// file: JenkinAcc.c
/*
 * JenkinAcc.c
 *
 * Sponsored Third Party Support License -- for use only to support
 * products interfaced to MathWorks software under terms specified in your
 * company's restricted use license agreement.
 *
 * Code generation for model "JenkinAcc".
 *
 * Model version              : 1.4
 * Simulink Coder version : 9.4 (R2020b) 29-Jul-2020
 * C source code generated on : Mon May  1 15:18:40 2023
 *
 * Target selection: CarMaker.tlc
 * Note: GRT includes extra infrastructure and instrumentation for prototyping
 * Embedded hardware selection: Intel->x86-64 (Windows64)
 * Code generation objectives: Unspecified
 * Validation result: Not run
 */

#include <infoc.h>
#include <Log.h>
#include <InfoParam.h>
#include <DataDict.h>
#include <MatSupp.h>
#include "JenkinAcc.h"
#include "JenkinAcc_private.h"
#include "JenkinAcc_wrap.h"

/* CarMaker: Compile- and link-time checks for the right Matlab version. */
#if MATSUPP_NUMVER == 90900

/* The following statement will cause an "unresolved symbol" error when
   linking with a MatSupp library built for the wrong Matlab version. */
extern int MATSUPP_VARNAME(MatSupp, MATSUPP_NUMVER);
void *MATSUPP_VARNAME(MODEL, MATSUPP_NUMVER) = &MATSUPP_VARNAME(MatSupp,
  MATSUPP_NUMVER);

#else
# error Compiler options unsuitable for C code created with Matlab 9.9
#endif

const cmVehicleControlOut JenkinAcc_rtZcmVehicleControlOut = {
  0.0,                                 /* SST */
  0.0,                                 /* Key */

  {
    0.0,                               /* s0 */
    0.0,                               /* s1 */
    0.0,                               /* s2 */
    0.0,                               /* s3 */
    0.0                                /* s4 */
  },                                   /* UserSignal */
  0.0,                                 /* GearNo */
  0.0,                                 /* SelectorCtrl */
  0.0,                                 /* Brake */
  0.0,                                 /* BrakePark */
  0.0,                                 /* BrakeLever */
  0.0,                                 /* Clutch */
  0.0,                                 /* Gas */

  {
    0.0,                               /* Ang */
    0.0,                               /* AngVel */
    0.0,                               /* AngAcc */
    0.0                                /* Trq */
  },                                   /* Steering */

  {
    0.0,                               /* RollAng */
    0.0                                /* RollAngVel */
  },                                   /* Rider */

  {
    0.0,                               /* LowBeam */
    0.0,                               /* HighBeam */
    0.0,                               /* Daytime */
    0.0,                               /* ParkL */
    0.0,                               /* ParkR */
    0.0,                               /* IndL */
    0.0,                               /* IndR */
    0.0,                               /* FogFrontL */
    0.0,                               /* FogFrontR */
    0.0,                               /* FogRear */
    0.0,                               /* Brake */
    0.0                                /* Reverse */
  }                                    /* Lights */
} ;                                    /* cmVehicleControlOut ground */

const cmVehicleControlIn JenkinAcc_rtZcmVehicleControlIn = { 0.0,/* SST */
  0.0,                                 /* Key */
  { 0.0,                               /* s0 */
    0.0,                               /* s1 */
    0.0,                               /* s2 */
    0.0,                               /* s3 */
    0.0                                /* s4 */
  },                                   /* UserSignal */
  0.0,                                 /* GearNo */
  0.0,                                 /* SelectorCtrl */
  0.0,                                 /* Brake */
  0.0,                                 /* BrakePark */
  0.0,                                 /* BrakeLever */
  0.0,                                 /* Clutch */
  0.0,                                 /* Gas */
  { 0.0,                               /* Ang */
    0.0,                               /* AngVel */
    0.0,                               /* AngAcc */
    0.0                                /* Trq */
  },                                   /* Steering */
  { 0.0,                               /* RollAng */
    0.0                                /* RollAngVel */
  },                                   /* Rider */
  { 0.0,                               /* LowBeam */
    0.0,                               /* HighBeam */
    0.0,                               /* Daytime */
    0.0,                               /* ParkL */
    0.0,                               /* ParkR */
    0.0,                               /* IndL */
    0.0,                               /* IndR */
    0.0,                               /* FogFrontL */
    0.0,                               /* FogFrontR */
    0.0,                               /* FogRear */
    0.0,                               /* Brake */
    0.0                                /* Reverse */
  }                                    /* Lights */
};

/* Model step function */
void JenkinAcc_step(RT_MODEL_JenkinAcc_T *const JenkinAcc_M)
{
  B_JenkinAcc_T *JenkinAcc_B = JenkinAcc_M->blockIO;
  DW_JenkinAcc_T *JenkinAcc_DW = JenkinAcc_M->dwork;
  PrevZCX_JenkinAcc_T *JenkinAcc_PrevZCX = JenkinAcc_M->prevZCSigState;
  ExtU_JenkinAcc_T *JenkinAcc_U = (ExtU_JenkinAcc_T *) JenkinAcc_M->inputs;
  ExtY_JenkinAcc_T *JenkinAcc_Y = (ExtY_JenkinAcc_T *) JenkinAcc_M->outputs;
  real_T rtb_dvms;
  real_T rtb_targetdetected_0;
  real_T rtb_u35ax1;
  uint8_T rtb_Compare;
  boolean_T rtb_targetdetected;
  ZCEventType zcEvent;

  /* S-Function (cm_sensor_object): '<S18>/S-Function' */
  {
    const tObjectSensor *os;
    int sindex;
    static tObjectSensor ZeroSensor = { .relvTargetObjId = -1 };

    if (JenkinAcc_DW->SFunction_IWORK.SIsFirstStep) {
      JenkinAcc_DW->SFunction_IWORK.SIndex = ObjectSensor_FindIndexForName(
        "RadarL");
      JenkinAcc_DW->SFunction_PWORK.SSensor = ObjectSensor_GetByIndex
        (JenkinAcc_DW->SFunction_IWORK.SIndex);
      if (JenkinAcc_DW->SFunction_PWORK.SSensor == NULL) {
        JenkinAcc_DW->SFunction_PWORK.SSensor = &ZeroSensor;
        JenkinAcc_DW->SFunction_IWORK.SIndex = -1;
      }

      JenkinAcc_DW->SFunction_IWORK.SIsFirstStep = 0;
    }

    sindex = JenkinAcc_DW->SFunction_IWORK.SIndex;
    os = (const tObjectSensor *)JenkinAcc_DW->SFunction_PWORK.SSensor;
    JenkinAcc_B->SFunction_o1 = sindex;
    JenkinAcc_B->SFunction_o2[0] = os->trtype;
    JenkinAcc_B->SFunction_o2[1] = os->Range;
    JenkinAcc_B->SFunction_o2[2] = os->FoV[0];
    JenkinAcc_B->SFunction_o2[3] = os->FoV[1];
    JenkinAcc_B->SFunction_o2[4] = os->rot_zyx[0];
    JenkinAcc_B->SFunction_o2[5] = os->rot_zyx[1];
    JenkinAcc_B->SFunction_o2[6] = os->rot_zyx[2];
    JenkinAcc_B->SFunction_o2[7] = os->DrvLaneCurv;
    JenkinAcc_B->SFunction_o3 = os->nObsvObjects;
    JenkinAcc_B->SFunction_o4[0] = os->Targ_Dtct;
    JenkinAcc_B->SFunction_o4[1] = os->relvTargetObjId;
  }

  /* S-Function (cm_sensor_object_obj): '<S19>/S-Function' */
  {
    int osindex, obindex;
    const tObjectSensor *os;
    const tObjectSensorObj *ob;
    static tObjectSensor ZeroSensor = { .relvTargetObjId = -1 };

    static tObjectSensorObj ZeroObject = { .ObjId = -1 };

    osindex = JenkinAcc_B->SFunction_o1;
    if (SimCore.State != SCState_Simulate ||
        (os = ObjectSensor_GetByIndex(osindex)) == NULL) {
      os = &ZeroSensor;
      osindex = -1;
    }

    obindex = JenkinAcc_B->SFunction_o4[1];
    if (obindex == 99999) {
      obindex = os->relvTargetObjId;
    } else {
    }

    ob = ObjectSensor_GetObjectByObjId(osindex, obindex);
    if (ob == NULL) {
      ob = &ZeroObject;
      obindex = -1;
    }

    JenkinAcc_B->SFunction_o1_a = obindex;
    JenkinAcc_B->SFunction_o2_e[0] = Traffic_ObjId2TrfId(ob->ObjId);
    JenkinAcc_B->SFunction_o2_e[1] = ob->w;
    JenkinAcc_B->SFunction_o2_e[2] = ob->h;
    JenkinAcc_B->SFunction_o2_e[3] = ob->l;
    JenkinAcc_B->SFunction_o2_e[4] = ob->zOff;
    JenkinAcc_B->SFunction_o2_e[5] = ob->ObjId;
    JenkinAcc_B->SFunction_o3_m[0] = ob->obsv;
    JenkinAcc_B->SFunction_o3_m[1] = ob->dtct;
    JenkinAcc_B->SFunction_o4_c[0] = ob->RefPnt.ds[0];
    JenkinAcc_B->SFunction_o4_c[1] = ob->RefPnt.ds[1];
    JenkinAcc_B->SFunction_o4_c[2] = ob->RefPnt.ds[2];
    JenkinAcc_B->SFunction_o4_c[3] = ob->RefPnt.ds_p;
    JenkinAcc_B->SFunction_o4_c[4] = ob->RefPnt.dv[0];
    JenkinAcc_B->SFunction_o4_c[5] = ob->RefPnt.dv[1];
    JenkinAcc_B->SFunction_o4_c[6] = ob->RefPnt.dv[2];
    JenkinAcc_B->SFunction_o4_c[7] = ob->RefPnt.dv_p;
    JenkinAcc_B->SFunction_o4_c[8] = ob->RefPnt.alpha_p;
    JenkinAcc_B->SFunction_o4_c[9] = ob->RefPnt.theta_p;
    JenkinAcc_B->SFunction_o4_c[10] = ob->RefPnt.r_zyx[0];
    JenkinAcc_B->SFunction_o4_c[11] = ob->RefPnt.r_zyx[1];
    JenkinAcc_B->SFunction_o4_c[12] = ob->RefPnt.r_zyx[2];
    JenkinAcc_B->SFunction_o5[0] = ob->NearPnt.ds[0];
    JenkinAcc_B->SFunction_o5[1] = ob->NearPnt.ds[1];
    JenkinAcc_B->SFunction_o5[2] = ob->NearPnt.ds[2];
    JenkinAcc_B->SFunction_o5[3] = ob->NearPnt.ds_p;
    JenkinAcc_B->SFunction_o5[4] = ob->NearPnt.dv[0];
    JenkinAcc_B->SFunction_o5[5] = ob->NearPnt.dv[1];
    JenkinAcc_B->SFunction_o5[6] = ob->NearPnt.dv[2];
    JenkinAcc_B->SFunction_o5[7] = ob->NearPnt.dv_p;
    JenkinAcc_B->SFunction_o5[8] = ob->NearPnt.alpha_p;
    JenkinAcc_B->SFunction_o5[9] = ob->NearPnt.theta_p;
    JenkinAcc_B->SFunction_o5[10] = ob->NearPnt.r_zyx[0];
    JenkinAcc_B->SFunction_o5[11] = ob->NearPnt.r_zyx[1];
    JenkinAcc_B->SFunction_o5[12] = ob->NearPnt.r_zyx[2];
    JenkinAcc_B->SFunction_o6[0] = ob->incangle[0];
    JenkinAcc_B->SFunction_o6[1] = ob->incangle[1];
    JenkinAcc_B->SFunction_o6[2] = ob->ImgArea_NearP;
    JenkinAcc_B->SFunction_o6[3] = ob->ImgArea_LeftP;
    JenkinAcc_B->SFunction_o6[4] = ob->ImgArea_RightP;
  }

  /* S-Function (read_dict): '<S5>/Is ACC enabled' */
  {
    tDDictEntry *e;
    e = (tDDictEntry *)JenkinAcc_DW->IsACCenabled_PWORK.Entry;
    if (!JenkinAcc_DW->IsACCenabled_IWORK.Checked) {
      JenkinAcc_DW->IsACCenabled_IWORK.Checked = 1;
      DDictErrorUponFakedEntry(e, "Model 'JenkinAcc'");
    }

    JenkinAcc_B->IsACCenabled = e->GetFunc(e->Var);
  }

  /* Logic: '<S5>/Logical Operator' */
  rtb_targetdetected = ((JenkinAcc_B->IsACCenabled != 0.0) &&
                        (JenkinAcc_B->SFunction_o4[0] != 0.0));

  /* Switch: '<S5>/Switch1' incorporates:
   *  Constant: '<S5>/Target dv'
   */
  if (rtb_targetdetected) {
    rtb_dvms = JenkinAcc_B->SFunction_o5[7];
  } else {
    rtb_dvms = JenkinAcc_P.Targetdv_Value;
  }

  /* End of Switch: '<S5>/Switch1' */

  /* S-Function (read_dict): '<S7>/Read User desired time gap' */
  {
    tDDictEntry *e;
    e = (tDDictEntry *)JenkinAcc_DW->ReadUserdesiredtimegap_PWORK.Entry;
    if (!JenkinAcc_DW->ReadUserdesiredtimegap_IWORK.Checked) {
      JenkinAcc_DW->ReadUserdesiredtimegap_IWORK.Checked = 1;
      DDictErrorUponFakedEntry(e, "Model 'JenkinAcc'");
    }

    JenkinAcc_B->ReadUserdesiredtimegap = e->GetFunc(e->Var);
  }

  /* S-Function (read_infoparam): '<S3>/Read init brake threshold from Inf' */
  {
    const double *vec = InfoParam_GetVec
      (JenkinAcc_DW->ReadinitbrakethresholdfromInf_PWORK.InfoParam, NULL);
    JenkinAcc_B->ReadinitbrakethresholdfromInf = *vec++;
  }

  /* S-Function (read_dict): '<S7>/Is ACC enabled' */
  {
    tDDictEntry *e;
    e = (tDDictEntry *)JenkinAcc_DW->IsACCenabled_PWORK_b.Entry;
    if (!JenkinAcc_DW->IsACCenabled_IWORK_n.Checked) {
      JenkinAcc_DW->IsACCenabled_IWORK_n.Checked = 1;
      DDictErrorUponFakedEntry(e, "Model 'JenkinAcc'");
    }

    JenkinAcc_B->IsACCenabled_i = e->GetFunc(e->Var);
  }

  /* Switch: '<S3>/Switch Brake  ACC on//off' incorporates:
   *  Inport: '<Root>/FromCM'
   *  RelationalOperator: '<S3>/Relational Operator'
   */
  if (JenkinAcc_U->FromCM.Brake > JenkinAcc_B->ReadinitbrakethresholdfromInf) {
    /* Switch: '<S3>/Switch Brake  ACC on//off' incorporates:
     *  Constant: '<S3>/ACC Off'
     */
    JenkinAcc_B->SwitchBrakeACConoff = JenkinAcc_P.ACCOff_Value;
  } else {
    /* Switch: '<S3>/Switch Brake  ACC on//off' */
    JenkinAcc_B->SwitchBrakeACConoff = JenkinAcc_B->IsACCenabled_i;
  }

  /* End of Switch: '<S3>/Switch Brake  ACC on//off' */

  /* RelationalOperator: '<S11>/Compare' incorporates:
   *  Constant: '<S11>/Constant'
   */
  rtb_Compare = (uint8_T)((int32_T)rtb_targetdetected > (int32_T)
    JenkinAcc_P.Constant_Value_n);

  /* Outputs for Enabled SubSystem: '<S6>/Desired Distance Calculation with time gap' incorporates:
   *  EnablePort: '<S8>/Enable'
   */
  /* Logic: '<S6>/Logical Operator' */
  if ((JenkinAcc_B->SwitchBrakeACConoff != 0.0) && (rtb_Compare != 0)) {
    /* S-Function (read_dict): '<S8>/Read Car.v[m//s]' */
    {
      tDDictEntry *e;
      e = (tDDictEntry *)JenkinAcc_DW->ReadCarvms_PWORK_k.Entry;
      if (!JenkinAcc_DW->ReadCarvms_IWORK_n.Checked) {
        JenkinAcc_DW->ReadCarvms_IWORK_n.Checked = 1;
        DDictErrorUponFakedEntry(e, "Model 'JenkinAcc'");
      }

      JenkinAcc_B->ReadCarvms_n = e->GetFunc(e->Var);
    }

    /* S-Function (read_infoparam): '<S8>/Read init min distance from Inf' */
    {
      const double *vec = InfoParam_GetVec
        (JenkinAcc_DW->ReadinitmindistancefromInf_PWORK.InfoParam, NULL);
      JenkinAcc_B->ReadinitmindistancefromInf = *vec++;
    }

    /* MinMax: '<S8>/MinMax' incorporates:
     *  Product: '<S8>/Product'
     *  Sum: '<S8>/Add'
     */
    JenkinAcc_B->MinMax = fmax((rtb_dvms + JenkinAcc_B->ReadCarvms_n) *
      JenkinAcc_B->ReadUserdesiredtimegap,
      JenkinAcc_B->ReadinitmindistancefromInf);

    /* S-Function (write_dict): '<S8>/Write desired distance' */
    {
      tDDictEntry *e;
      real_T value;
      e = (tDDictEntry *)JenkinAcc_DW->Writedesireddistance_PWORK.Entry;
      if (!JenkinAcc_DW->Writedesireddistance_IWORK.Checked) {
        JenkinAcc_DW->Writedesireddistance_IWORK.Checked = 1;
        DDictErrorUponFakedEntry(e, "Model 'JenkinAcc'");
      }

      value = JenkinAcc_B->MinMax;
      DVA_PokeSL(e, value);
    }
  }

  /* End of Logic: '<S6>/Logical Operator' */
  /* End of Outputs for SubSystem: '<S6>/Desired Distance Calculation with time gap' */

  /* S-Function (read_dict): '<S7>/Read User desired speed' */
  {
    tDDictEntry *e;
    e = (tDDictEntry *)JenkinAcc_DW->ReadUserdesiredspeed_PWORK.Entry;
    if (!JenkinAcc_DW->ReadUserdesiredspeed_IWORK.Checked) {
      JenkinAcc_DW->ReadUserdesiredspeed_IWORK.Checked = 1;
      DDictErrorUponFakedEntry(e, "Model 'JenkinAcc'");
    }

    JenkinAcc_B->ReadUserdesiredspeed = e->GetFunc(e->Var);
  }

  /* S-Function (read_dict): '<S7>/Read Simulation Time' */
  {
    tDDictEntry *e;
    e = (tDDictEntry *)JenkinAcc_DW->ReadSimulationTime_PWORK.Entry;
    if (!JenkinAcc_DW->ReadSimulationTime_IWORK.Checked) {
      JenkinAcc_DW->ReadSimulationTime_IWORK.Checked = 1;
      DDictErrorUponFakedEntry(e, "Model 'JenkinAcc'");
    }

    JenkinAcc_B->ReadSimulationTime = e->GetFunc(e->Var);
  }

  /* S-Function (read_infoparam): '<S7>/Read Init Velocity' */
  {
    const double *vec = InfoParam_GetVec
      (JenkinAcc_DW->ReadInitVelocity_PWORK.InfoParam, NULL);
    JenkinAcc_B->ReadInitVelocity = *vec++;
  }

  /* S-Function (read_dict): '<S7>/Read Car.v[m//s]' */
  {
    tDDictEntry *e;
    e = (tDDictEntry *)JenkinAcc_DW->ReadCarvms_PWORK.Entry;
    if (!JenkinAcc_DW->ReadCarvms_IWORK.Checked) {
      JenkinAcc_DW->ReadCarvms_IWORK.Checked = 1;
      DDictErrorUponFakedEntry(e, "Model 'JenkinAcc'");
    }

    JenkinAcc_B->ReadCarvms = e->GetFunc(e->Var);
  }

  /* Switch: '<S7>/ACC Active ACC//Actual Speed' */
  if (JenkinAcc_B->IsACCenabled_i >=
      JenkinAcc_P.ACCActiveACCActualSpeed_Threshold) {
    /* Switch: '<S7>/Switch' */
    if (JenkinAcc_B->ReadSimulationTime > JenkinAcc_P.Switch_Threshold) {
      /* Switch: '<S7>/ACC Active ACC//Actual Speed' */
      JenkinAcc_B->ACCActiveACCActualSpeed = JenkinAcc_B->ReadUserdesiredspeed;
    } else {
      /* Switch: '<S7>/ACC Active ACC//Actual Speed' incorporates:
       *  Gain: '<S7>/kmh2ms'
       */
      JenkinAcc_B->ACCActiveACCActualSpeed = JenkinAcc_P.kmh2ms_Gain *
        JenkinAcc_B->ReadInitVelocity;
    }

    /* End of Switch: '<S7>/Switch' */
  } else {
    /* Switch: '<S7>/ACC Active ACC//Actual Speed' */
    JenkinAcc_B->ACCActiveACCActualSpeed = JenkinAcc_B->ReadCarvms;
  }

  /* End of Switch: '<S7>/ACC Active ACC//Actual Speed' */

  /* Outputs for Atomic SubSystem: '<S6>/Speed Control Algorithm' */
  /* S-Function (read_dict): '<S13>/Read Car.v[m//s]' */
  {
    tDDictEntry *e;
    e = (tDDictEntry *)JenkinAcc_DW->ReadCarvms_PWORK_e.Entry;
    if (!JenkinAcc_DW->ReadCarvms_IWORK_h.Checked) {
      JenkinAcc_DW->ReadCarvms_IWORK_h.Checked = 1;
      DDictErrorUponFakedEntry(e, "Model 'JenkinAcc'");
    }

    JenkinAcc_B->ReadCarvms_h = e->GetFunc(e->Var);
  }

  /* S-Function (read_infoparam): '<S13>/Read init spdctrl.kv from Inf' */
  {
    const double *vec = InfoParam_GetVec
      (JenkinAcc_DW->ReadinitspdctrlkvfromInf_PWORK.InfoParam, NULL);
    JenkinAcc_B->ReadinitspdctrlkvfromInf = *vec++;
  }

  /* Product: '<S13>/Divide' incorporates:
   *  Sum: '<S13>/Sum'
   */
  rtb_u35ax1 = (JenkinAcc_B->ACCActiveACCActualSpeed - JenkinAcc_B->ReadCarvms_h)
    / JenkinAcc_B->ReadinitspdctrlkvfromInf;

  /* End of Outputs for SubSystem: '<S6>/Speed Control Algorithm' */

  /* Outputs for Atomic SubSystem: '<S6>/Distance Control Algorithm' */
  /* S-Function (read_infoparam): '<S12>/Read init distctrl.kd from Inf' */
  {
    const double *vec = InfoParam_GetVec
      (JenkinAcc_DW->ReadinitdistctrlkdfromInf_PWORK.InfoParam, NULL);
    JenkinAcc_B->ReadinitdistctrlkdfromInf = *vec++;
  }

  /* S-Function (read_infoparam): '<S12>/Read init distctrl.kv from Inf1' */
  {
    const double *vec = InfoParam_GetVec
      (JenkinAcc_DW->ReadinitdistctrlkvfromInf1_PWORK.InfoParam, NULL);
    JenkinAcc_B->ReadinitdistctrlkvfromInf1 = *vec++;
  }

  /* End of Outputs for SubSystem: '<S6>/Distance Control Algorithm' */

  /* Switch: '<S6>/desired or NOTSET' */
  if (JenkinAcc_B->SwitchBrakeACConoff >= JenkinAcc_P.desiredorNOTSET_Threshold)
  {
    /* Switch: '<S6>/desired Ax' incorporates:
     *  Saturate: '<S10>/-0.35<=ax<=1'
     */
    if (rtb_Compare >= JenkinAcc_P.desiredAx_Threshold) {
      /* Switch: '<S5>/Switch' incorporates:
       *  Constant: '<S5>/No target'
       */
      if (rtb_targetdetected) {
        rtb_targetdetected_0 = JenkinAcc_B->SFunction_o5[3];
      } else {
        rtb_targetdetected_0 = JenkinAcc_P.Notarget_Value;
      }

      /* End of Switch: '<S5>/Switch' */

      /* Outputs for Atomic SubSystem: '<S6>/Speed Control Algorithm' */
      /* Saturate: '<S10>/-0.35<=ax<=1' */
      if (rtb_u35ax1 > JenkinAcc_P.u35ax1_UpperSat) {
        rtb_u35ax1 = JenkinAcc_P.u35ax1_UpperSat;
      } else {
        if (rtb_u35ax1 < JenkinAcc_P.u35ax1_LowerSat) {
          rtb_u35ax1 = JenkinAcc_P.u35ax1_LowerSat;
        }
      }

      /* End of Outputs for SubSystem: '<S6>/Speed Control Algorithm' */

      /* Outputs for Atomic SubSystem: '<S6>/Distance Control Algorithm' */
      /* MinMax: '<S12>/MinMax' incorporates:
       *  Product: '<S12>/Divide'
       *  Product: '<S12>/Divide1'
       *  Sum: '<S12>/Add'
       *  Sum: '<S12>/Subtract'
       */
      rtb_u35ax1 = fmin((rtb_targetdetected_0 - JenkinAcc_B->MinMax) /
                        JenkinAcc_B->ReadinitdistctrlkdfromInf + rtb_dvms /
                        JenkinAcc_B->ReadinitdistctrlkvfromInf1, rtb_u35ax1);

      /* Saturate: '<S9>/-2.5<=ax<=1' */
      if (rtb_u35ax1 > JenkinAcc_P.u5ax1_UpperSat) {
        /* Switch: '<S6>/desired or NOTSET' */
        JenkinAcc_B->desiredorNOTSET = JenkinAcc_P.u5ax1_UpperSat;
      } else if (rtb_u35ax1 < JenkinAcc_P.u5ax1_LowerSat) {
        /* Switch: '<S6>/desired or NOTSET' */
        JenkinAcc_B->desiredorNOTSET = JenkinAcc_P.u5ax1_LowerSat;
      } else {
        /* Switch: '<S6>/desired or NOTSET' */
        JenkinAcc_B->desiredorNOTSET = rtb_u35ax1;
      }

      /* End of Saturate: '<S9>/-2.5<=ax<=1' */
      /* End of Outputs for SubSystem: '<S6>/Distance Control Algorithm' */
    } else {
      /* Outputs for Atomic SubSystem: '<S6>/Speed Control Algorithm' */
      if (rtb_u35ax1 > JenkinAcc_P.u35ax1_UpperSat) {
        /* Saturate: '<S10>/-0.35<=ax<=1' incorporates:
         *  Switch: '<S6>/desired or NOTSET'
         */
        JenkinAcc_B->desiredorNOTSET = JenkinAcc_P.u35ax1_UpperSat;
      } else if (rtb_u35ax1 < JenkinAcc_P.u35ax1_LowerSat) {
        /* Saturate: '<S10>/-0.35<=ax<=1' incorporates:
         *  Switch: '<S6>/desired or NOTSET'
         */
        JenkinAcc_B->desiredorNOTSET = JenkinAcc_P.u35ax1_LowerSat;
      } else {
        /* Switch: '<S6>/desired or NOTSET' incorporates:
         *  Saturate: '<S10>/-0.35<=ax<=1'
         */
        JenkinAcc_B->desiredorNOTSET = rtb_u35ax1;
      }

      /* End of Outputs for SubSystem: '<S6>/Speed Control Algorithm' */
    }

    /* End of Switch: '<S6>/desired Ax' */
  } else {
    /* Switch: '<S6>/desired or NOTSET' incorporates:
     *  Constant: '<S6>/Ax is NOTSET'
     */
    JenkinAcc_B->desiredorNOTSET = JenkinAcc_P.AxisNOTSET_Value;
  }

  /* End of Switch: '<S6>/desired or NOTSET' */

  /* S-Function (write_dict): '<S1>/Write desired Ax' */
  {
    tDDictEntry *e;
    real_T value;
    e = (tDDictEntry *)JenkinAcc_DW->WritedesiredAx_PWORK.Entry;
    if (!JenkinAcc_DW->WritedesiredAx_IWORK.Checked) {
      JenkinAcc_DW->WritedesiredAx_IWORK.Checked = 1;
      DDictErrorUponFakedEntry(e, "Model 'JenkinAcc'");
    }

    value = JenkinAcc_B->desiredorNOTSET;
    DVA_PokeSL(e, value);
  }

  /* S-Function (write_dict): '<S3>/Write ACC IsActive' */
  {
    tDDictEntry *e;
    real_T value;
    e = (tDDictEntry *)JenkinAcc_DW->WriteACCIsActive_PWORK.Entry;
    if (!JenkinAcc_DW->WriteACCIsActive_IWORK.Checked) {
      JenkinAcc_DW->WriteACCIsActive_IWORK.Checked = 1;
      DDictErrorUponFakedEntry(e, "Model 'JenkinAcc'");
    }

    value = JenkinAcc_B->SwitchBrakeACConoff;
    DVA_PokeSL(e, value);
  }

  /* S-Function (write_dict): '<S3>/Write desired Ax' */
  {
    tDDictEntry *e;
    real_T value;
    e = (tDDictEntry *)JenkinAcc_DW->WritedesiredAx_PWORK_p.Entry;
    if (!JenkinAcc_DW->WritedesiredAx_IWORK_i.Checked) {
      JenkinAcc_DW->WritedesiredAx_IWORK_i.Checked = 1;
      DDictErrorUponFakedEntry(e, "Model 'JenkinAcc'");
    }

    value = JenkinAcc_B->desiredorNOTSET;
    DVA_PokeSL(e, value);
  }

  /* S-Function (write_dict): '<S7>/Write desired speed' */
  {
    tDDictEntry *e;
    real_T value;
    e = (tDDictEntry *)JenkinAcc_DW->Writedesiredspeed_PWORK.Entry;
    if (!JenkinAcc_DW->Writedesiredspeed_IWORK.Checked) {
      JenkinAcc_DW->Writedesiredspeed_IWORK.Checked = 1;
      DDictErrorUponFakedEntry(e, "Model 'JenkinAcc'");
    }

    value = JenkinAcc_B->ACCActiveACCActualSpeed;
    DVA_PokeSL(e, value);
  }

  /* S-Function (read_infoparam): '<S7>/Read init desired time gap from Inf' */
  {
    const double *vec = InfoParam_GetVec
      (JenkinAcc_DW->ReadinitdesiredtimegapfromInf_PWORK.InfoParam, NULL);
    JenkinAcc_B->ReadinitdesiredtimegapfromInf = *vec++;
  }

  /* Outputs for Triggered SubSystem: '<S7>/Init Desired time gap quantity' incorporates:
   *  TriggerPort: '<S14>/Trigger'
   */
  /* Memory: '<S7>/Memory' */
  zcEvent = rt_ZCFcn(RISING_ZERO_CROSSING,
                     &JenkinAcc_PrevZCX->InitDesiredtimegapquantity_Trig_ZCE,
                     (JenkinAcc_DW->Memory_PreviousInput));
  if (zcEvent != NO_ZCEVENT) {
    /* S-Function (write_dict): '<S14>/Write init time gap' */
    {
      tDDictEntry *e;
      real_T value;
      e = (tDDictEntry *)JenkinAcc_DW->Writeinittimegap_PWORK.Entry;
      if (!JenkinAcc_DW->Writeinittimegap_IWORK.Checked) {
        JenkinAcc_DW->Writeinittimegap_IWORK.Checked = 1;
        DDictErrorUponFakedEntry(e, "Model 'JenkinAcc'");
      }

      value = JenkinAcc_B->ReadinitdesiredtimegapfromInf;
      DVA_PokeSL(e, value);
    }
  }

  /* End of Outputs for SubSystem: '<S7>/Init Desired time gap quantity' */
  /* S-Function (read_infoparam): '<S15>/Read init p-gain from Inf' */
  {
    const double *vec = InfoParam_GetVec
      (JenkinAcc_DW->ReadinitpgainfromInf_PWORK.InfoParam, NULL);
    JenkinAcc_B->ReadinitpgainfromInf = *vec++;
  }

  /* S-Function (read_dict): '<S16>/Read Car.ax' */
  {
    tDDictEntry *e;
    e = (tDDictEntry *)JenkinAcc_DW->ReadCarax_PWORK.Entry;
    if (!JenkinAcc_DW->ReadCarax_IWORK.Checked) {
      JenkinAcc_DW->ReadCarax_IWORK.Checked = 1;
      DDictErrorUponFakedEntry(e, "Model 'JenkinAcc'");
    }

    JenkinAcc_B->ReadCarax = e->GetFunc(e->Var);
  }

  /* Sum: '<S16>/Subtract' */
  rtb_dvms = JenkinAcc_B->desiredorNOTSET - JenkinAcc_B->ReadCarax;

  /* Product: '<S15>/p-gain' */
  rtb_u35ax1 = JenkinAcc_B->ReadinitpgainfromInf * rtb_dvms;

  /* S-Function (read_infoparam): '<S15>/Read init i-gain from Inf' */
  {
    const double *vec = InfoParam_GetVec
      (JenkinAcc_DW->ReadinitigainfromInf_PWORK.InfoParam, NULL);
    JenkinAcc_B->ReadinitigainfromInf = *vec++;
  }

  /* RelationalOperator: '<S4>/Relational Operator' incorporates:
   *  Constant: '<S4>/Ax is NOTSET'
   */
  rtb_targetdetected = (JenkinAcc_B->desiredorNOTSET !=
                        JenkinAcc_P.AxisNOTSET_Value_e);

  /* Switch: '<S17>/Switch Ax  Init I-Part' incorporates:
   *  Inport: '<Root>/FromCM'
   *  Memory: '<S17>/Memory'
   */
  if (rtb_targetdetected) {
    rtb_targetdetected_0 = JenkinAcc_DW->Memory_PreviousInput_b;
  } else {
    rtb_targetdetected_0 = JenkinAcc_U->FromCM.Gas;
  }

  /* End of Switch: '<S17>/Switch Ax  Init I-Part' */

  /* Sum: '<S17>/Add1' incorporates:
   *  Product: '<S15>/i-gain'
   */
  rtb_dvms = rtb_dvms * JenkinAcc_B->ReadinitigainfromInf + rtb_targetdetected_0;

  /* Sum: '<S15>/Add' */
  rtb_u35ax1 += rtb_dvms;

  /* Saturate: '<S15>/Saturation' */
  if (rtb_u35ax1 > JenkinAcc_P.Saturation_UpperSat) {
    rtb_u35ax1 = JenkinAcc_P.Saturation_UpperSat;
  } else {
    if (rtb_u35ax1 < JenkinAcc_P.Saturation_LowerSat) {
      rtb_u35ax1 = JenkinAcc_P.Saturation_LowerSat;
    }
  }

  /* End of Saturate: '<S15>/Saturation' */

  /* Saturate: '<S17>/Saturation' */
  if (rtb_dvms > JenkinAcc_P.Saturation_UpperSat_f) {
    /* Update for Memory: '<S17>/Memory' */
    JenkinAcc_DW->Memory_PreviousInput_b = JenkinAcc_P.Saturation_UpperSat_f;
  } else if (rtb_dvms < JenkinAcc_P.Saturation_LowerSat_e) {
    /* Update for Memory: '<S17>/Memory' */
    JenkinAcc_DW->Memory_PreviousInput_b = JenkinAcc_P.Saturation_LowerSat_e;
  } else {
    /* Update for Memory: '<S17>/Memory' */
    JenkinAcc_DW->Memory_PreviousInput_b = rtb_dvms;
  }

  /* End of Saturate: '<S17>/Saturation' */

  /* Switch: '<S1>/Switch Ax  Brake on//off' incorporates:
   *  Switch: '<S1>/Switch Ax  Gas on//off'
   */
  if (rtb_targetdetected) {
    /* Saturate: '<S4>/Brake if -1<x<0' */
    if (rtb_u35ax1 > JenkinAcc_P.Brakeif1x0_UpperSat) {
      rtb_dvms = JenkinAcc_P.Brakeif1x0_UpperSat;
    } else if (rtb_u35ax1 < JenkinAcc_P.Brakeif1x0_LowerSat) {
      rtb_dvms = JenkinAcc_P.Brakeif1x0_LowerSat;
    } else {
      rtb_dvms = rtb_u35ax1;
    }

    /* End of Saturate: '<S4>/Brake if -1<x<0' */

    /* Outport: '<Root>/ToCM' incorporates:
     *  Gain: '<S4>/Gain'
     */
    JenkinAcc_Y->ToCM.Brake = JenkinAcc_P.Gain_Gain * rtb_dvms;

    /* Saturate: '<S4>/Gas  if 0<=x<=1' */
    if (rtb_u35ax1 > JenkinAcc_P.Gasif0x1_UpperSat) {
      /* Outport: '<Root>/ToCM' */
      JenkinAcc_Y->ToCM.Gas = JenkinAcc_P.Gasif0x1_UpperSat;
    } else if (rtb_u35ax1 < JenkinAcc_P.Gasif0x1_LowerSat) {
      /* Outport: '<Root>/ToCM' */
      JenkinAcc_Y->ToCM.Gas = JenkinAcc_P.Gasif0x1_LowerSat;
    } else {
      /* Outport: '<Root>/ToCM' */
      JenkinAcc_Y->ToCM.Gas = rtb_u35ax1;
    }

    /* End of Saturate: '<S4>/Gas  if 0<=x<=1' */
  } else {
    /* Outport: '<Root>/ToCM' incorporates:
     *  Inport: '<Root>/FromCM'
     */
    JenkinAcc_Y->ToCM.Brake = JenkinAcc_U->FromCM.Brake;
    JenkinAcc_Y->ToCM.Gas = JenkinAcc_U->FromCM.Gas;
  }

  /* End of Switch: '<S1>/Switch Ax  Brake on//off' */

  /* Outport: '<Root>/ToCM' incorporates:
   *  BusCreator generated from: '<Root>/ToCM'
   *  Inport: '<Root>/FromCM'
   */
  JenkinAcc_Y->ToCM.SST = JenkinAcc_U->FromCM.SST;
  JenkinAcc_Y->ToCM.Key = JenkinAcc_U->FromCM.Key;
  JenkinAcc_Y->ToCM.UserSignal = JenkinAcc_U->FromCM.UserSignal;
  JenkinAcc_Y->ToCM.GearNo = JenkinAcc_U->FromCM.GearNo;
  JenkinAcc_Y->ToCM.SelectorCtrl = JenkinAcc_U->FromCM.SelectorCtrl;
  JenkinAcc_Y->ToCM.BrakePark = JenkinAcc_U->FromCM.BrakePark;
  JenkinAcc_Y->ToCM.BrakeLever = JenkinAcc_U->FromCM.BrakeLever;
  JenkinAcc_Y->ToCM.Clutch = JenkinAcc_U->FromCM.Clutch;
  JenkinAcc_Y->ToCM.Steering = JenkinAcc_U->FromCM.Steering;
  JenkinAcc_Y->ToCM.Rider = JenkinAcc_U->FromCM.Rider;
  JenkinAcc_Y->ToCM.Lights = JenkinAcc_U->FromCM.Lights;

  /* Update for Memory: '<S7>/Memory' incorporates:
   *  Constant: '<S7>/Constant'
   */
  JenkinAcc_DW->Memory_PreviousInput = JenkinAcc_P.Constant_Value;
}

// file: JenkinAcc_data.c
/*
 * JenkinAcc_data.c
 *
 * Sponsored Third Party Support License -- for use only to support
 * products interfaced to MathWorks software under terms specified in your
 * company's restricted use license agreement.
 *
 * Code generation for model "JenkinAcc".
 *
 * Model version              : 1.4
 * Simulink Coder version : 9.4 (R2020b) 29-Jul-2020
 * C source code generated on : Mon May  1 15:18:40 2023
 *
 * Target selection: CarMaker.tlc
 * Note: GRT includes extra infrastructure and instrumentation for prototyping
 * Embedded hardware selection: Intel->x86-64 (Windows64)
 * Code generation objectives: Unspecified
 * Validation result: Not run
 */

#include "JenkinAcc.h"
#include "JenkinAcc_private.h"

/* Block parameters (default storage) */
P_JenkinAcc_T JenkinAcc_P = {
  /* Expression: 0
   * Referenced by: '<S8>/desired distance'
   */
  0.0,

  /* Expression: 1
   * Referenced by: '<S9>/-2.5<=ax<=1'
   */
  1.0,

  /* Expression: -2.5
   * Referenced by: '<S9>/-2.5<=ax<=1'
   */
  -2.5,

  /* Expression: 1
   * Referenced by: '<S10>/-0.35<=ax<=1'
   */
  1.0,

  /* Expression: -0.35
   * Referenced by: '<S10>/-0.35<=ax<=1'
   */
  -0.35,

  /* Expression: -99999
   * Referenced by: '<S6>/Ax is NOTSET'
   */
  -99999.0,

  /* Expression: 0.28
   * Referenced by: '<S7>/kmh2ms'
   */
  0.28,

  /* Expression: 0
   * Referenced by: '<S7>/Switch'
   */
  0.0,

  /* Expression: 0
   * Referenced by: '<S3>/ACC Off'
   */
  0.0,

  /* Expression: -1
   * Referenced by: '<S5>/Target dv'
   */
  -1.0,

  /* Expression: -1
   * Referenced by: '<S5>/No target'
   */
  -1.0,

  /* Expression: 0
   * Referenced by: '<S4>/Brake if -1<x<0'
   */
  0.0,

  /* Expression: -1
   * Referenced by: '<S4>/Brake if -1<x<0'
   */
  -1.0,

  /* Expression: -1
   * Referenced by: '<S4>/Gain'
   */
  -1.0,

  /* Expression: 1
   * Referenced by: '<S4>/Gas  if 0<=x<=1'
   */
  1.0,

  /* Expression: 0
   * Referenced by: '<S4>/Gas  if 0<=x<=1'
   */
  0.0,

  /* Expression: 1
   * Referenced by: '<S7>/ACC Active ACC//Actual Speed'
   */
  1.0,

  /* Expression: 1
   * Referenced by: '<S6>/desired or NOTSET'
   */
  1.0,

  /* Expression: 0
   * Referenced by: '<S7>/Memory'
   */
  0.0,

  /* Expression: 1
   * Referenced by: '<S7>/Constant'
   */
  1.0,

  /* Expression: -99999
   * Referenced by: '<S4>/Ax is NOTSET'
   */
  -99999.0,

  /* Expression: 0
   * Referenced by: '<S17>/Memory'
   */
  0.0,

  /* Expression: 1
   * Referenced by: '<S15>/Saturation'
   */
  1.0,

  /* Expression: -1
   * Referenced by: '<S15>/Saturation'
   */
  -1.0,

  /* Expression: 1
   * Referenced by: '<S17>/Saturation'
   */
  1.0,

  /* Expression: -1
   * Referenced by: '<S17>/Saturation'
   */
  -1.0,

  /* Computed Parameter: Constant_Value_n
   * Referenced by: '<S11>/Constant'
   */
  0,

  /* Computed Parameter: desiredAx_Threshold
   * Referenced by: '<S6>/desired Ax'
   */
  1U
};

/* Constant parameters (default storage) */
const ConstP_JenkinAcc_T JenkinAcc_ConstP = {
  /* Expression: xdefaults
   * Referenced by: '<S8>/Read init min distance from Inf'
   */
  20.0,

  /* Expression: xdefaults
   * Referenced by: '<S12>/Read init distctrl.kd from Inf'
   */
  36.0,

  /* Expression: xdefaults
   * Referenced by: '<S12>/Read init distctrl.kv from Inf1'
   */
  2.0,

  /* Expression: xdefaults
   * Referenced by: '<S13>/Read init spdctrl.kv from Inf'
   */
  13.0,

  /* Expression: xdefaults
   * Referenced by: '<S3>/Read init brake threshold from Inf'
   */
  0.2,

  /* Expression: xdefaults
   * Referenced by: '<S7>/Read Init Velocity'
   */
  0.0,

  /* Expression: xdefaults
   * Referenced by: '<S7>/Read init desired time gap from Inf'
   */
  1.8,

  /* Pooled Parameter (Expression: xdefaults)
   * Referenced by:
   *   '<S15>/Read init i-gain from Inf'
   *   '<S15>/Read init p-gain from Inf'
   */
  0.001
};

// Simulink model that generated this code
simulink model "JenkinAcc"  (R2020b)
settings: Solver=ode1  StartTime=0.0  StopTime=inf  FixedStep=0.001  RelTol=1e-3
PreLoadFcn:
  | vehicle = 'Car'; if ~length(which('cmself')), cmenv; end
  | JenkinAcc_bus
InitFcn:
  | vehicle = 'Car'; if ~length(which('cmself')), cmenv; end
  | JenkinAcc_bus
libraries: CarMaker4SL x32, simulink x1

== system JenkinAcc ==
  FromCM : Inport  OutDataTypeStr=Bus: cmVehicleControlIn
  AccelCtrl : Subsystem
  IF_In_Selector : BusSelector  OutputSignals=SST,Key,UserSignal.s0,UserSignal.s1,UserSignal.s2,UserSignal.s3,UserSignal.s4,GearNo,SelectorCtrl,Brake,BrakePark,BrakeLever,Clutch,Gas,Steering.Ang,Steering.AngVel,Steering.AngAcc,Steering.Trq,Rider.RollAng,Rider.RollAngVel,Lights.LowBeam,Lights.HighBeam,Lights.Daytime,Lights.ParkL,Lights.ParkR,Lights.IndL,Lights.IndR,Lights.FogFrontL,Lights.FogFrontR,Lights.FogRear,Lights.Brake,Lights.Reverse
  IF_Out_Selector : Subsystem  mask(Signal Selection){}
      mask help: Signal Selection Block
  ToCM : Outport  OutDataTypeStr=Bus: cmVehicleControlOut
  wires:
  FromCM/1 -> IF_In_Selector/1
  IF_Out_Selector/1(ToCM) -> ToCM/1
  IF_In_Selector/8 -> IF_Out_Selector/8(GearNo)  "<GearNo>"
  IF_In_Selector/9 -> IF_Out_Selector/9(SelectorCtrl)  "<SelectorCtrl>"
  IF_In_Selector/7 -> IF_Out_Selector/7(UserSignal.s4)  "<s4>"
  IF_In_Selector/6 -> IF_Out_Selector/6(UserSignal.s3)  "<s3>"
  IF_In_Selector/11 -> IF_Out_Selector/11(BrakePark)  "<BrakePark>"
  IF_In_Selector/5 -> IF_Out_Selector/5(UserSignal.s2)  "<s2>"
  IF_In_Selector/12 -> IF_Out_Selector/12(BrakeLever)  "<BrakeLever>"
  IF_In_Selector/4 -> IF_Out_Selector/4(UserSignal.s1)  "<s1>"
  IF_In_Selector/13 -> IF_Out_Selector/13(Clutch)  "<Clutch>"
  IF_In_Selector/3 -> IF_Out_Selector/3(UserSignal.s0)  "<s0>"
  IF_In_Selector/2 -> IF_Out_Selector/2(Key)  "<Key>"
  IF_In_Selector/15 -> IF_Out_Selector/15(Steering.Ang)  "<Ang>"
  IF_In_Selector/1 -> IF_Out_Selector/1(SST)  "<SST>"
  IF_In_Selector/16 -> IF_Out_Selector/16(Steering.AngVel)  "<AngVel>"
  IF_In_Selector/17 -> IF_Out_Selector/17(Steering.AngAcc)  "<AngAcc>"
  IF_In_Selector/18 -> IF_Out_Selector/18(Steering.Trq)  "<Trq>"
  IF_In_Selector/19 -> IF_Out_Selector/19(Rider.RollAng)  "<RollAng>"
  IF_In_Selector/20 -> IF_Out_Selector/20(Rider.RollAngVel)  "<RollAngVel>"
  IF_In_Selector/21 -> IF_Out_Selector/21(Lights.LowBeam)  "<LowBeam>"
  IF_In_Selector/22 -> IF_Out_Selector/22(Lights.HighBeam)  "<HighBeam>"
  IF_In_Selector/23 -> IF_Out_Selector/23(Lights.Daytime)  "<Daytime>"
  IF_In_Selector/24 -> IF_Out_Selector/24(Lights.ParkL)  "<ParkL>"
  IF_In_Selector/25 -> IF_Out_Selector/25(Lights.ParkR)  "<ParkR>"
  IF_In_Selector/26 -> IF_Out_Selector/26(Lights.IndL)  "<IndL>"
  IF_In_Selector/27 -> IF_Out_Selector/27(Lights.IndR)  "<IndR>"
  IF_In_Selector/28 -> IF_Out_Selector/28(Lights.FogFrontL)  "<FogFrontL>"
  IF_In_Selector/29 -> IF_Out_Selector/29(Lights.FogFrontR)  "<FogFrontR>"
  IF_In_Selector/30 -> IF_Out_Selector/30(Lights.FogRear)  "<FogRear>"
  IF_In_Selector/31 -> IF_Out_Selector/31(Lights.Brake)  "<Brake>"
  IF_In_Selector/14 -> AccelCtrl/2(DM Gas)  "<Gas>"
  IF_In_Selector/10 -> AccelCtrl/1(DM Brake)  "<Brake>"
  AccelCtrl/1(VC Brake) -> IF_Out_Selector/10(Brake)
  AccelCtrl/2(VC Gas) -> IF_Out_Selector/14(Gas)
  IF_In_Selector/32 -> IF_Out_Selector/32(Lights.Reverse)  "<Reverse>"

== system JenkinAcc/AccelCtrl ==
  DM Brake : Inport
  DM Gas : Inport  Port=2
  ACC ECU : Subsystem
  AccelCtrl : Subsystem
  Define CM Dict : CarMaker4SL/Define CM Dict  xname=AccelCtrl.ACC.IsActive  xmono=off  xtype=Char  xdvaplace=DM  xnstates=2  xfirststate=0  xinitial=1
  Define CM Dict1 : CarMaker4SL/Define CM Dict  xname=AccelCtrl.ACC.DesiredTGap  xunit=s  xmono=off  xtype=Double4  xdvaplace=DM  xnstates=0  xfirststate=0  xinitial=0
  Define CM Dict2 : CarMaker4SL/Define CM Dict  xname=AccelCtrl.ACC.DesiredSpd  xunit=m/s  xmono=off  xtype=Double4  xdvaplace=DM  xnstates=0  xfirststate=0  xinitial=0
  Define CM Dict3 : CarMaker4SL/Define CM Dict  xname=AccelCtrl.ACC.DesiredAx  xunit=m/s^2  xmono=off  xtype=Double4  xdvaplace=DM  xnstates=0  xfirststate=0  xinitial=0
  Define CM Dict4 : CarMaker4SL/Define CM Dict  xname=AccelCtrl.DesiredAx  xunit=m/s^2  xmono=off  xtype=Double4  xdvaplace=DM  xnstates=0  xfirststate=0  xinitial=0
  Define CM Dict5 : CarMaker4SL/Define CM Dict  xname=AccelCtrl.ACC.DesiredDist  xunit=m  xmono=off  xtype=Double4  xdvaplace=DM  xnstates=0  xfirststate=0  xinitial=0
  Sensor : Subsystem
  Switch Ax Brake on/off : Switch  Threshold=1  SaturateOnIntegerOverflow=on
  Switch Ax Gas on/off : Switch  Threshold=1  SaturateOnIntegerOverflow=on
  Write desired Ax : CarMaker4SL/Write CM Dict  xname=AccelCtrl.DesiredAx  xsync=off
  VC Brake : Outport  VectorParamsAs1DForOutWhenUnconnected=off
  VC Gas : Outport  Port=2  VectorParamsAs1DForOutWhenUnconnected=off
  wires:
  Sensor/1(relevant target) -> ACC ECU/1(ACC Target)
  DM Brake/1 -> Switch Ax Brake on/off/3, ACC ECU/2(DM Brake)
  Switch Ax Gas on/off/1 -> VC Gas/1
  Switch Ax Brake on/off/1 -> VC Brake/1
  AccelCtrl/1(Gas Out) -> Switch Ax Gas on/off/1
  AccelCtrl/3(Brake Out) -> Switch Ax Brake on/off/1
  ACC ECU/1(Desired Ax) -> AccelCtrl/1(Desired Ax), Write desired Ax/1
  DM Gas/1 -> Switch Ax Gas on/off/3, AccelCtrl/2(DM Gas)
  AccelCtrl/2(AxCtrl On) -> Switch Ax Gas on/off/2, Switch Ax Brake on/off/2

== system JenkinAcc/IF_Out_Selector ==
  SST : Inport
  Key : Inport  Port=2
  UserSignal.s0 : Inport  Port=3
  UserSignal.s1 : Inport  Port=4
  UserSignal.s2 : Inport  Port=5
  UserSignal.s3 : Inport  Port=6
  UserSignal.s4 : Inport  Port=7
  GearNo : Inport  Port=8
  SelectorCtrl : Inport  Port=9
  Brake : Inport  Port=10
  BrakePark : Inport  Port=11
  BrakeLever : Inport  Port=12
  Clutch : Inport  Port=13
  Gas : Inport  Port=14
  Steering.Ang : Inport  Port=15
  Steering.AngVel : Inport  Port=16
  Steering.AngAcc : Inport  Port=17
  Steering.Trq : Inport  Port=18
  Rider.RollAng : Inport  Port=19
  Rider.RollAngVel : Inport  Port=20
  Lights.LowBeam : Inport  Port=21
  Lights.HighBeam : Inport  Port=22
  Lights.Daytime : Inport  Port=23
  Lights.ParkL : Inport  Port=24
  Lights.ParkR : Inport  Port=25
  Lights.IndL : Inport  Port=26
  Lights.IndR : Inport  Port=27
  Lights.FogFrontL : Inport  Port=28
  Lights.FogFrontR : Inport  Port=29
  Lights.FogRear : Inport  Port=30
  Lights.Brake : Inport  Port=31
  Lights.Reverse : Inport  Port=32
  Lights : BusCreator  Inputs=12
  RateTransition : RateTransition  OutPortSampleTime=str2num(get_param(bdroot,'FixedStep'))
  Rider : BusCreator  Inputs=2
  Steering : BusCreator  Inputs=4
  UserSignal : BusCreator  Inputs=5
  cmVehicleControlOut : BusCreator  Inputs=13
  ToCM : Outport
  wires:
  RateTransition/1 -> ToCM/1
  cmVehicleControlOut/1 -> RateTransition/1
  UserSignal/1 -> cmVehicleControlOut/3  "UserSignal"
  Steering/1 -> cmVehicleControlOut/11  "Steering"
  Rider/1 -> cmVehicleControlOut/12  "Rider"
  Lights/1 -> cmVehicleControlOut/13  "Lights"
  Brake/1 -> cmVehicleControlOut/6  "Brake"
  Gas/1 -> cmVehicleControlOut/10  "Gas"
  SST/1 -> cmVehicleControlOut/1  "SST"
  Key/1 -> cmVehicleControlOut/2  "Key"
  UserSignal.s0/1 -> UserSignal/1  "s0"
  UserSignal.s1/1 -> UserSignal/2  "s1"
  UserSignal.s2/1 -> UserSignal/3  "s2"
  UserSignal.s3/1 -> UserSignal/4  "s3"
  UserSignal.s4/1 -> UserSignal/5  "s4"
  GearNo/1 -> cmVehicleControlOut/4  "GearNo"
  SelectorCtrl/1 -> cmVehicleControlOut/5  "SelectorCtrl"
  BrakePark/1 -> cmVehicleControlOut/7  "BrakePark"
  BrakeLever/1 -> cmVehicleControlOut/8  "BrakeLever"
  Clutch/1 -> cmVehicleControlOut/9  "Clutch"
  Steering.Ang/1 -> Steering/1  "Ang"
  Steering.AngVel/1 -> Steering/2  "AngVel"
  Steering.AngAcc/1 -> Steering/3  "AngAcc"
  Steering.Trq/1 -> Steering/4  "Trq"
  Rider.RollAng/1 -> Rider/1  "RollAng"
  Rider.RollAngVel/1 -> Rider/2  "RollAngVel"
  Lights.LowBeam/1 -> Lights/1  "LowBeam"
  Lights.HighBeam/1 -> Lights/2  "HighBeam"
  Lights.Daytime/1 -> Lights/3  "Daytime"
  Lights.ParkL/1 -> Lights/4  "ParkL"
  Lights.ParkR/1 -> Lights/5  "ParkR"
  Lights.IndL/1 -> Lights/6  "IndL"
  Lights.IndR/1 -> Lights/7  "IndR"
  Lights.FogFrontL/1 -> Lights/8  "FogFrontL"
  Lights.FogFrontR/1 -> Lights/9  "FogFrontR"
  Lights.FogRear/1 -> Lights/10  "FogRear"
  Lights.Brake/1 -> Lights/11  "Brake"
  Lights.Reverse/1 -> Lights/12  "Reverse"

== system JenkinAcc/AccelCtrl/ACC ECU ==
  ACC Target : Inport
  DM Brake : Inport  Port=2
  ACC Control : Subsystem
  ACC Off : Constant  Value=0
  ACC User Input : Subsystem
  Bus Selector : BusSelector  OutputSignals=target detected,ds[m],dv[m/s]
  Read init brake threshold from Inf : CarMaker4SL/Read CM Parameter  xfile=Vehicle  xkey=AccelCtrl.ACC.BrakeThreshold  xnout=1  xdefaults=0.2  xmuxed=off  xstime=Continuous
  Relational Operator : RelationalOperator  Operator=>  RndMeth=Nearest
  Switch Brake ACC on/off : Switch  Threshold=1  SaturateOnIntegerOverflow=on
  Write ACC IsActive : CarMaker4SL/Write CM Dict  xname=AccelCtrl.ACC.IsActive  xsync=off
  Write desired Ax : CarMaker4SL/Write CM Dict  xname=AccelCtrl.ACC.DesiredAx  xsync=off
  Desired Ax : Outport  VectorParamsAs1DForOutWhenUnconnected=off
  wires:
  ACC Target/1 -> Bus Selector/1
  Bus Selector/2 -> ACC Control/3(Target.ds)  "<ds[m]>"
  Bus Selector/3 -> ACC Control/4(Target.dv)  "<dv[m/s]>"
  Bus Selector/1 -> ACC Control/2(Target Dtct)  "<target detected>"
  ACC Control/1(Desired Ax) -> Desired Ax/1, Write desired Ax/1
  ACC User Input/2(Desired time gap[s]) -> ACC Control/5(Desired time gap)
  ACC User Input/3(Desired speed[m/s]) -> ACC Control/6(Desired speed)
  DM Brake/1 -> Relational Operator/1
  ACC User Input/1(ACC enabled) -> Switch Brake ACC on/off/3
  Relational Operator/1 -> Switch Brake ACC on/off/2
  ACC Off/1 -> Switch Brake ACC on/off/1
  Switch Brake ACC on/off/1 -> ACC Control/1(ACC enabled), Write ACC IsActive/1
  Read init brake threshold from Inf/1 -> Relational Operator/2

== system JenkinAcc/AccelCtrl/AccelCtrl ==
  note: x
  note: x
  Desired Ax : Inport
  DM Gas : Inport  Port=2
  Ax is NOTSET : Constant  Value=-99999
  Brake if -1<x<0 : Saturate  UpperLimit=0  LowerLimit=-1
  Gain : Gain  Gain=-1  SaturateOnIntegerOverflow=on  OutDataTypeStr=Inherit: Same as input  ParamDataTypeStr=Inherit: Same as input
  Gas  if 0<=x<=1 : Saturate  UpperLimit=1  LowerLimit=0
  PI-Controller : Subsystem
  Relational Operator : RelationalOperator  Operator=~=  RndMeth=Nearest
  "controlled process variable " : Subsystem
  Gas Out : Outport  VectorParamsAs1DForOutWhenUnconnected=off
  AxCtrl On : Outport  Port=2  VectorParamsAs1DForOutWhenUnconnected=off
  Brake Out : Outport  Port=3  VectorParamsAs1DForOutWhenUnconnected=off
  wires:
  Gain/1 -> Brake Out/1
  "controlled process variable "/1(delta ax) -> PI-Controller/1(delta_ax)
  DM Gas/1 -> PI-Controller/2(DM_Gas)
  Desired Ax/1 -> "controlled process variable "/1(desired ax), Relational Operator/1
  PI-Controller/1(Gas or Brake) -> Brake if -1<x<0/1, Gas  if 0<=x<=1/1
  Gas  if 0<=x<=1/1 -> Gas Out/1
  Brake if -1<x<0/1 -> Gain/1
  Ax is NOTSET/1 -> Relational Operator/2
  Relational Operator/1 -> AxCtrl On/1, PI-Controller/3(AxCtrl On)

== system JenkinAcc/AccelCtrl/Sensor ==
  note: No handling of
      | input parameters with Simulink.
      | All calculations are at C level.
      | Access to relevant target
      | over CarMaker DataDict quantities.
  note: relevant target detected
  Bus Creator : BusCreator  Inputs=3
  Bus Selector : BusSelector  OutputSignals=relvTargetIndex,TargetDetected
  Bus Selector1 : BusSelector  OutputSignals=NearPnt ds_p,NearPnt dv_p
  Car ObjectSensor : CarMaker4SL/Sensors/Object Sensor  xname=RadarL  xstime=Continuous
  Car ObjectSensor Object : CarMaker4SL/Sensors/Object Sensor Object  xname=INPORT  ximode=World Objects  xstime=Continuous
  Ground : Ground
  Is ACC enabled : CarMaker4SL/Read CM Dict  xname=AccelCtrl.ACC.IsActive  xsync=off  xstime=Continuous
  Logical Operator : Logic  AllPortsSameDT=off
  No target : Constant  Value=-1
  Switch : Switch  Criteria=u2 > Threshold  SaturateOnIntegerOverflow=on
  Switch1 : Switch  Criteria=u2 > Threshold  SaturateOnIntegerOverflow=on
  Target dv : Constant  Value=-1
  Terminator{,1..6} (7 alike) : Terminator
  relevant target : Outport  VectorParamsAs1DForOutWhenUnconnected=off
  wires:
  Switch/1 -> Bus Creator/2  "ds[m]"
  Bus Selector1/1 -> Switch/1  "<NearPnt ds_p>"
  No target/1 -> Switch/3
  Bus Selector1/2 -> Switch1/1  "<NearPnt dv_p>"
  Target dv/1 -> Switch1/3
  Switch1/1 -> Bus Creator/3  "dv[m/s]"
  Bus Creator/1 -> relevant target/1
  Is ACC enabled/1 -> Logical Operator/1
  Logical Operator/1 -> Bus Creator/1, Switch1/2, Switch/2  "target detected"
  Car ObjectSensor/1 -> Car ObjectSensor Object/1
  Ground/1 -> Car ObjectSensor/1
  Car ObjectSensor/4 -> Bus Selector/1
  Bus Selector/2 -> Logical Operator/2  "<TargetDetected>"
  Bus Selector/1 -> Car ObjectSensor Object/2  "<relvTargetIndex>"
  Car ObjectSensor Object/5 -> Bus Selector1/1
  Car ObjectSensor/2 -> Terminator/1
  Car ObjectSensor/3 -> Terminator1/1
  Car ObjectSensor Object/1 -> Terminator2/1
  Car ObjectSensor Object/2 -> Terminator3/1
  Car ObjectSensor Object/3 -> Terminator4/1
  Car ObjectSensor Object/4 -> Terminator5/1
  Car ObjectSensor Object/6 -> Terminator6/1

== system JenkinAcc/AccelCtrl/ACC ECU/ACC Control ==
  ACC enabled : Inport
  Target Dtct : Inport  Port=2
  Target.ds : Inport  Port=3
  Target.dv : Inport  Port=4
  Desired time gap : Inport  Port=5
  Desired speed : Inport  Port=6
  Ax is NOTSET : Constant  Value=-99999
  Desired Distance Calculation with time gap : Subsystem  TreatAsAtomicUnit=on
  Distance Control Algorithm : Subsystem  TreatAsAtomicUnit=on
  Logical Operator : Logic  AllPortsSameDT=off
  Speed Control Algorithm : Subsystem  TreatAsAtomicUnit=on
  Target detected : simulink/Logic and Bit Operations/Compare To Zero  relop=>  OutDataTypeStr=uint8  ZeroCross=off
  desired Ax : Switch  Threshold=1  SaturateOnIntegerOverflow=on
  desired or NOTSET : Switch  Threshold=1  SaturateOnIntegerOverflow=on
  Desired Ax : Outport  VectorParamsAs1DForOutWhenUnconnected=off
  wires:
  Target.dv/1 -> Distance Control Algorithm/2(Target.dv[m/s]), Desired Distance Calculation with time gap/1(Target.dv)
  Target.ds/1 -> Distance Control Algorithm/1(Target.ds[m])
  Target Dtct/1 -> Target detected/1
  Distance Control Algorithm/1("  limited ax") -> desired Ax/1
  Target detected/1 -> desired Ax/2, Logical Operator/2
  Desired Distance Calculation with time gap/1(desired distance) -> Distance Control Algorithm/3(desired distance[m])
  Desired time gap/1 -> Desired Distance Calculation with time gap/2(desired time gap)
  Desired speed/1 -> Speed Control Algorithm/1(desire speed[m/s])
  Speed Control Algorithm/1(ax speed control) -> desired Ax/3, Distance Control Algorithm/4(ax speed control)
  ACC enabled/1 -> Logical Operator/1, desired or NOTSET/2
  Logical Operator/1 -> Desired Distance Calculation with time gap/Enable
  desired or NOTSET/1 -> Desired Ax/1
  desired Ax/1 -> desired or NOTSET/1
  Ax is NOTSET/1 -> desired or NOTSET/3

== system JenkinAcc/AccelCtrl/ACC ECU/ACC User Input ==
  ACC Active ACC/Actual Speed : Switch  Threshold=1  SaturateOnIntegerOverflow=on
  Constant : Constant
  Init Desired time gap quantity : Subsystem  TreatAsAtomicUnit=on
  Is ACC enabled : CarMaker4SL/Read CM Dict  xname=AccelCtrl.ACC.IsActive  xsync=off  xstime=Continuous
  Memory : Memory
  Read Car.v[m/s] : CarMaker4SL/Read CM Dict  xname=Car.v  xsync=off  xstime=Continuous
  Read Init Velocity : CarMaker4SL/Read CM Parameter  xfile=Testrun  xkey=DrivMan.Init.Velocity  xnout=1  xdefaults=0  xmuxed=on  xstime=Continuous
  Read Simulation Time : CarMaker4SL/Read CM Dict  xname=Time  xsync=off  xstime=Continuous
  Read User desired speed : CarMaker4SL/Read CM Dict  xname=AccelCtrl.ACC.DesiredSpd  xsync=off  xstime=Continuous
  Read User desired time gap : CarMaker4SL/Read CM Dict  xname=AccelCtrl.ACC.DesiredTGap  xsync=off  xstime=Continuous
  Read init desired time gap from Inf : CarMaker4SL/Read CM Parameter  xfile=Vehicle  xkey=AccelCtrl.ACC.DesrTGap  xnout=1  xdefaults=1.8  xmuxed=off  xstime=Continuous
  Switch : Switch  Criteria=u2 > Threshold
  Write desired speed : CarMaker4SL/Write CM Dict  xname=AccelCtrl.ACC.DesiredSpd  xsync=off
  kmh2ms : Gain  Gain=0.28
  ACC enabled : Outport  VectorParamsAs1DForOutWhenUnconnected=off
  Desired time gap[s] : Outport  Port=2  VectorParamsAs1DForOutWhenUnconnected=off
  Desired speed[m/s] : Outport  Port=3  VectorParamsAs1DForOutWhenUnconnected=off
  wires:
  Is ACC enabled/1 -> ACC enabled/1, ACC Active ACC/Actual Speed/2
  Read Car.v[m/s]/1 -> ACC Active ACC/Actual Speed/3
  ACC Active ACC/Actual Speed/1 -> Desired speed[m/s]/1, Write desired speed/1
  Read User desired time gap/1 -> Desired time gap[s]/1
  Constant/1 -> Memory/1
  Memory/1 -> Init Desired time gap quantity/Trigger
  Read init desired time gap from Inf/1 -> Init Desired time gap quantity/1("Init desired time gap ")
  Read Init Velocity/1 -> kmh2ms/1
  Switch/1 -> ACC Active ACC/Actual Speed/1
  Read User desired speed/1 -> Switch/1
  Read Simulation Time/1 -> Switch/2
  kmh2ms/1 -> Switch/3

== system JenkinAcc/AccelCtrl/AccelCtrl/PI-Controller ==
  delta_ax : Inport
  DM_Gas : Inport  Port=2
  AxCtrl On : Inport  Port=3
  Add : Sum  SaturateOnIntegerOverflow=on  OutDataTypeStr=Inherit: Same as first input
  Integrator : Subsystem
  Read init i-gain from Inf : CarMaker4SL/Read CM Parameter  xfile=Vehicle  xkey=AccelCtrl.i  xnout=1  xdefaults=0.001  xmuxed=off  xstime=Continuous
  Read init p-gain from Inf : CarMaker4SL/Read CM Parameter  xfile=Vehicle  xkey=AccelCtrl.p  xnout=1  xdefaults=0.001  xmuxed=off  xstime=Continuous
  Saturation : Saturate  UpperLimit=1  LowerLimit=-1
  i-gain : Product  SaturateOnIntegerOverflow=on  OutDataTypeStr=Inherit: Same as first input
  p-gain : Product  SaturateOnIntegerOverflow=on  OutDataTypeStr=Inherit: Same as first input
  Gas or Brake : Outport  VectorParamsAs1DForOutWhenUnconnected=off
  wires:
  Saturation/1 -> Gas or Brake/1
  Add/1 -> Saturation/1
  p-gain/1 -> Add/1
  delta_ax/1 -> p-gain/2, i-gain/1
  i-gain/1 -> Integrator/1(I-Part)
  AxCtrl On/1 -> Integrator/2(AxCtrl On)
  DM_Gas/1 -> Integrator/3(Init I-part)
  Integrator/1("I-part tot ") -> Add/2
  Read init p-gain from Inf/1 -> p-gain/1
  Read init i-gain from Inf/1 -> i-gain/2

== system JenkinAcc/AccelCtrl/AccelCtrl/controlled process variable  ==
  desired ax : Inport
  Read Car.ax : CarMaker4SL/Read CM Dict  xname=Car.ax  xsync=off  xstime=Continuous
  Subtract : Sum  Inputs=+-  SaturateOnIntegerOverflow=on
  delta ax : Outport  VectorParamsAs1DForOutWhenUnconnected=off
  wires:
  desired ax/1 -> Subtract/1
  Read Car.ax/1 -> Subtract/2
  Subtract/1 -> delta ax/1

== system JenkinAcc/AccelCtrl/ACC ECU/ACC Control/Desired Distance Calculation with time gap ==
  Target.dv : Inport
  desired time gap : Inport  Port=2
  Enable : EnablePort
  Add : Sum  SaturateOnIntegerOverflow=on  OutDataTypeStr=Inherit: Same as first input
  MinMax : MinMax  Function=max  Inputs=2  InputSameDT=on  SaturateOnIntegerOverflow=on
  Product : Product  SaturateOnIntegerOverflow=on  OutDataTypeStr=Inherit: Same as first input
  Read Car.v[m/s] : CarMaker4SL/Read CM Dict  xname=Car.v  xsync=off  xstime=Continuous
  Read init min distance from Inf : CarMaker4SL/Read CM Parameter  xfile=Vehicle  xkey=AccelCtrl.ACC.DistMin  xnout=1  xdefaults=20  xmuxed=off  xstime=Continuous
  Write desired distance : CarMaker4SL/Write CM Dict  xname=AccelCtrl.ACC.DesiredDist  xsync=off
  desired distance : Outport  InitialOutput=0  VectorParamsAs1DForOutWhenUnconnected=off
  wires:
  Read Car.v[m/s]/1 -> Add/2
  Product/1 -> MinMax/1
  Add/1 -> Product/2
  desired time gap/1 -> Product/1
  Target.dv/1 -> Add/1
  MinMax/1 -> desired distance/1, Write desired distance/1
  Read init min distance from Inf/1 -> MinMax/2

== system JenkinAcc/AccelCtrl/ACC ECU/ACC Control/Distance Control Algorithm ==
  Target.ds[m] : Inport
  Target.dv[m/s] : Inport  Port=2
  desired distance[m] : Inport  Port=3
  ax speed control : Inport  Port=4
  -2.5<=ax<=1 : Saturate  UpperLimit=1  LowerLimit=-2.5
  desired ax : Subsystem
  "  limited ax" : Outport  InitialOutput=0  VectorParamsAs1DForOutWhenUnconnected=off
  wires:
  ax speed control/1 -> desired ax/4(ax speed control)
  desired distance[m]/1 -> desired ax/3(desired distance[m])
  Target.dv[m/s]/1 -> desired ax/2(Target.dv[m/s])
  Target.ds[m]/1 -> desired ax/1(Target.ds[m])
  -2.5<=ax<=1/1 -> "  limited ax"/1
  desired ax/1(desired ax) -> -2.5<=ax<=1/1

== system JenkinAcc/AccelCtrl/ACC ECU/ACC Control/Speed Control Algorithm ==
  desire speed[m/s] : Inport
  -0.35<=ax<=1 : Saturate  UpperLimit=1  LowerLimit=-0.35
  desired ax : Subsystem
  ax speed control : Outport  InitialOutput=0  VectorParamsAs1DForOutWhenUnconnected=off
  wires:
  desire speed[m/s]/1 -> desired ax/1(desire speed[m/s])
  desired ax/1(desired ax) -> -0.35<=ax<=1/1
  -0.35<=ax<=1/1 -> ax speed control/1

== system JenkinAcc/AccelCtrl/ACC ECU/ACC User Input/Init Desired time gap quantity ==
  "Init desired time gap " : Inport
  Trigger : TriggerPort  VariantControl=Variant
  Write init time gap : CarMaker4SL/Write CM Dict  xname=AccelCtrl.ACC.DesiredTGap  xsync=off
  wires:
  "Init desired time gap "/1 -> Write init time gap/1

== system JenkinAcc/AccelCtrl/AccelCtrl/PI-Controller/Integrator ==
  I-Part : Inport
  AxCtrl On : Inport  Port=2
  Init I-part : Inport  Port=3
  Add1 : Sum  SaturateOnIntegerOverflow=on  OutDataTypeStr=Inherit: Same as first input
  Memory : Memory
  Saturation : Saturate  UpperLimit=1  LowerLimit=-1
  Switch Ax Init I-Part : Switch  Threshold=1  SaturateOnIntegerOverflow=on
  "I-part tot " : Outport  VectorParamsAs1DForOutWhenUnconnected=off
  wires:
  Saturation/1 -> Memory/1
  Switch Ax Init I-Part/1 -> Add1/2
  Add1/1 -> Saturation/1, "I-part tot "/1
  I-Part/1 -> Add1/1
  AxCtrl On/1 -> Switch Ax Init I-Part/2
  Memory/1 -> Switch Ax Init I-Part/1
  Init I-part/1 -> Switch Ax Init I-Part/3

== system JenkinAcc/AccelCtrl/ACC ECU/ACC Control/Distance Control Algorithm/desired ax ==
  note: desired ax = (target.ds-desired.distance)/(kd)+target.dv/kv
  note: delta_ds
  Target.ds[m] : Inport
  Target.dv[m/s] : Inport  Port=2
  desired distance[m] : Inport  Port=3
  ax speed control : Inport  Port=4
  Add : Sum  SaturateOnIntegerOverflow=on  OutDataTypeStr=Inherit: Same as first input
  Divide : Product  Inputs=*/  SaturateOnIntegerOverflow=on  OutDataTypeStr=Inherit: Same as first input
  Divide1 : Product  Inputs=*/  SaturateOnIntegerOverflow=on  OutDataTypeStr=Inherit: Same as first input
  MinMax : MinMax  Inputs=2  InputSameDT=on  SaturateOnIntegerOverflow=on
  Read init distctrl.kd from Inf : CarMaker4SL/Read CM Parameter  xfile=Vehicle  xkey=AccelCtrl.ACC.DistCtrl.kd  xnout=1  xdefaults=36  xmuxed=off  xstime=Continuous
  Read init distctrl.kv from Inf1 : CarMaker4SL/Read CM Parameter  xfile=Vehicle  xkey=AccelCtrl.ACC.DistCtrl.kv  xnout=1  xdefaults=2  xmuxed=off  xstime=Continuous
  Subtract : Sum  Inputs=+-  SaturateOnIntegerOverflow=on  OutDataTypeStr=Inherit: Same as first input
  desired ax : Outport  VectorParamsAs1DForOutWhenUnconnected=off
  wires:
  MinMax/1 -> desired ax/1
  ax speed control/1 -> MinMax/2
  Add/1 -> MinMax/1
  Divide1/1 -> Add/2
  Divide/1 -> Add/1
  Subtract/1 -> Divide/1
  desired distance[m]/1 -> Subtract/2
  Target.ds[m]/1 -> Subtract/1
  Target.dv[m/s]/1 -> Divide1/1
  Read init distctrl.kd from Inf/1 -> Divide/2
  Read init distctrl.kv from Inf1/1 -> Divide1/2

== system JenkinAcc/AccelCtrl/ACC ECU/ACC Control/Speed Control Algorithm/desired ax ==
  desire speed[m/s] : Inport
  Divide : Product  Inputs=*/  SaturateOnIntegerOverflow=on  OutDataTypeStr=Inherit: Same as first input
  Read Car.v[m/s] : CarMaker4SL/Read CM Dict  xname=Car.v  xsync=off  xstime=Continuous
  Read init spdctrl.kv from Inf : CarMaker4SL/Read CM Parameter  xfile=Vehicle  xkey=AccelCtrl.ACC.SpdCtrl.kv  xnout=1  xdefaults=13  xmuxed=off  xstime=Continuous
  Sum : Sum  Inputs=|+-  SaturateOnIntegerOverflow=on  OutDataTypeStr=Inherit: Same as first input
  desired ax : Outport  VectorParamsAs1DForOutWhenUnconnected=off
  wires:
  Divide/1 -> desired ax/1
  desire speed[m/s]/1 -> Sum/1
  Read Car.v[m/s]/1 -> Sum/2
  Sum/1 -> Divide/1
  Read init spdctrl.kv from Inf/1 -> Divide/2
